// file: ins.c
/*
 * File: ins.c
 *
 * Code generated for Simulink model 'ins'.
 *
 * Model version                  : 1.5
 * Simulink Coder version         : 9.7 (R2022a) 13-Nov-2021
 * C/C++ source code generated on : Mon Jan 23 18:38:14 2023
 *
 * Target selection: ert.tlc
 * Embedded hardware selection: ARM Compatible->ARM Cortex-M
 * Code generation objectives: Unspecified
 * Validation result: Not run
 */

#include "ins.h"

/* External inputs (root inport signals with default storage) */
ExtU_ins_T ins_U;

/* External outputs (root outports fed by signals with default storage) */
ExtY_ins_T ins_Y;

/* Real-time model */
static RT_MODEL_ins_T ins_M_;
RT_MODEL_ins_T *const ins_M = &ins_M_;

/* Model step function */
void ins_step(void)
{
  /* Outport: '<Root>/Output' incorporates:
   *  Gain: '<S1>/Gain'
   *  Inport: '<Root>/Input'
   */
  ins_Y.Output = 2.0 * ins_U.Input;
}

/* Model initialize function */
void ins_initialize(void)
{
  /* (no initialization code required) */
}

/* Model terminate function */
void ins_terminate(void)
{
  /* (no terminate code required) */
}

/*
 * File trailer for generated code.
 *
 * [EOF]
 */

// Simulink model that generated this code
simulink model "ins"  (R2022a)
settings: Solver=FixedStepDiscrete  StartTime=0.0  StopTime=10  RelTol=1e-3  EnableMultiTasking=on

== system ins ==
  Input : Inport
  Subsystem : Subsystem
  Output : Outport
  wires:
  Input/1 -> Subsystem/1(In1)
  Subsystem/1(Output) -> Output/1

== system ins/Subsystem ==
  In1 : Inport
  Gain : Gain  Gain=2
  Output : Outport
  wires:
  In1/1 -> Gain/1
  Gain/1 -> Output/1
